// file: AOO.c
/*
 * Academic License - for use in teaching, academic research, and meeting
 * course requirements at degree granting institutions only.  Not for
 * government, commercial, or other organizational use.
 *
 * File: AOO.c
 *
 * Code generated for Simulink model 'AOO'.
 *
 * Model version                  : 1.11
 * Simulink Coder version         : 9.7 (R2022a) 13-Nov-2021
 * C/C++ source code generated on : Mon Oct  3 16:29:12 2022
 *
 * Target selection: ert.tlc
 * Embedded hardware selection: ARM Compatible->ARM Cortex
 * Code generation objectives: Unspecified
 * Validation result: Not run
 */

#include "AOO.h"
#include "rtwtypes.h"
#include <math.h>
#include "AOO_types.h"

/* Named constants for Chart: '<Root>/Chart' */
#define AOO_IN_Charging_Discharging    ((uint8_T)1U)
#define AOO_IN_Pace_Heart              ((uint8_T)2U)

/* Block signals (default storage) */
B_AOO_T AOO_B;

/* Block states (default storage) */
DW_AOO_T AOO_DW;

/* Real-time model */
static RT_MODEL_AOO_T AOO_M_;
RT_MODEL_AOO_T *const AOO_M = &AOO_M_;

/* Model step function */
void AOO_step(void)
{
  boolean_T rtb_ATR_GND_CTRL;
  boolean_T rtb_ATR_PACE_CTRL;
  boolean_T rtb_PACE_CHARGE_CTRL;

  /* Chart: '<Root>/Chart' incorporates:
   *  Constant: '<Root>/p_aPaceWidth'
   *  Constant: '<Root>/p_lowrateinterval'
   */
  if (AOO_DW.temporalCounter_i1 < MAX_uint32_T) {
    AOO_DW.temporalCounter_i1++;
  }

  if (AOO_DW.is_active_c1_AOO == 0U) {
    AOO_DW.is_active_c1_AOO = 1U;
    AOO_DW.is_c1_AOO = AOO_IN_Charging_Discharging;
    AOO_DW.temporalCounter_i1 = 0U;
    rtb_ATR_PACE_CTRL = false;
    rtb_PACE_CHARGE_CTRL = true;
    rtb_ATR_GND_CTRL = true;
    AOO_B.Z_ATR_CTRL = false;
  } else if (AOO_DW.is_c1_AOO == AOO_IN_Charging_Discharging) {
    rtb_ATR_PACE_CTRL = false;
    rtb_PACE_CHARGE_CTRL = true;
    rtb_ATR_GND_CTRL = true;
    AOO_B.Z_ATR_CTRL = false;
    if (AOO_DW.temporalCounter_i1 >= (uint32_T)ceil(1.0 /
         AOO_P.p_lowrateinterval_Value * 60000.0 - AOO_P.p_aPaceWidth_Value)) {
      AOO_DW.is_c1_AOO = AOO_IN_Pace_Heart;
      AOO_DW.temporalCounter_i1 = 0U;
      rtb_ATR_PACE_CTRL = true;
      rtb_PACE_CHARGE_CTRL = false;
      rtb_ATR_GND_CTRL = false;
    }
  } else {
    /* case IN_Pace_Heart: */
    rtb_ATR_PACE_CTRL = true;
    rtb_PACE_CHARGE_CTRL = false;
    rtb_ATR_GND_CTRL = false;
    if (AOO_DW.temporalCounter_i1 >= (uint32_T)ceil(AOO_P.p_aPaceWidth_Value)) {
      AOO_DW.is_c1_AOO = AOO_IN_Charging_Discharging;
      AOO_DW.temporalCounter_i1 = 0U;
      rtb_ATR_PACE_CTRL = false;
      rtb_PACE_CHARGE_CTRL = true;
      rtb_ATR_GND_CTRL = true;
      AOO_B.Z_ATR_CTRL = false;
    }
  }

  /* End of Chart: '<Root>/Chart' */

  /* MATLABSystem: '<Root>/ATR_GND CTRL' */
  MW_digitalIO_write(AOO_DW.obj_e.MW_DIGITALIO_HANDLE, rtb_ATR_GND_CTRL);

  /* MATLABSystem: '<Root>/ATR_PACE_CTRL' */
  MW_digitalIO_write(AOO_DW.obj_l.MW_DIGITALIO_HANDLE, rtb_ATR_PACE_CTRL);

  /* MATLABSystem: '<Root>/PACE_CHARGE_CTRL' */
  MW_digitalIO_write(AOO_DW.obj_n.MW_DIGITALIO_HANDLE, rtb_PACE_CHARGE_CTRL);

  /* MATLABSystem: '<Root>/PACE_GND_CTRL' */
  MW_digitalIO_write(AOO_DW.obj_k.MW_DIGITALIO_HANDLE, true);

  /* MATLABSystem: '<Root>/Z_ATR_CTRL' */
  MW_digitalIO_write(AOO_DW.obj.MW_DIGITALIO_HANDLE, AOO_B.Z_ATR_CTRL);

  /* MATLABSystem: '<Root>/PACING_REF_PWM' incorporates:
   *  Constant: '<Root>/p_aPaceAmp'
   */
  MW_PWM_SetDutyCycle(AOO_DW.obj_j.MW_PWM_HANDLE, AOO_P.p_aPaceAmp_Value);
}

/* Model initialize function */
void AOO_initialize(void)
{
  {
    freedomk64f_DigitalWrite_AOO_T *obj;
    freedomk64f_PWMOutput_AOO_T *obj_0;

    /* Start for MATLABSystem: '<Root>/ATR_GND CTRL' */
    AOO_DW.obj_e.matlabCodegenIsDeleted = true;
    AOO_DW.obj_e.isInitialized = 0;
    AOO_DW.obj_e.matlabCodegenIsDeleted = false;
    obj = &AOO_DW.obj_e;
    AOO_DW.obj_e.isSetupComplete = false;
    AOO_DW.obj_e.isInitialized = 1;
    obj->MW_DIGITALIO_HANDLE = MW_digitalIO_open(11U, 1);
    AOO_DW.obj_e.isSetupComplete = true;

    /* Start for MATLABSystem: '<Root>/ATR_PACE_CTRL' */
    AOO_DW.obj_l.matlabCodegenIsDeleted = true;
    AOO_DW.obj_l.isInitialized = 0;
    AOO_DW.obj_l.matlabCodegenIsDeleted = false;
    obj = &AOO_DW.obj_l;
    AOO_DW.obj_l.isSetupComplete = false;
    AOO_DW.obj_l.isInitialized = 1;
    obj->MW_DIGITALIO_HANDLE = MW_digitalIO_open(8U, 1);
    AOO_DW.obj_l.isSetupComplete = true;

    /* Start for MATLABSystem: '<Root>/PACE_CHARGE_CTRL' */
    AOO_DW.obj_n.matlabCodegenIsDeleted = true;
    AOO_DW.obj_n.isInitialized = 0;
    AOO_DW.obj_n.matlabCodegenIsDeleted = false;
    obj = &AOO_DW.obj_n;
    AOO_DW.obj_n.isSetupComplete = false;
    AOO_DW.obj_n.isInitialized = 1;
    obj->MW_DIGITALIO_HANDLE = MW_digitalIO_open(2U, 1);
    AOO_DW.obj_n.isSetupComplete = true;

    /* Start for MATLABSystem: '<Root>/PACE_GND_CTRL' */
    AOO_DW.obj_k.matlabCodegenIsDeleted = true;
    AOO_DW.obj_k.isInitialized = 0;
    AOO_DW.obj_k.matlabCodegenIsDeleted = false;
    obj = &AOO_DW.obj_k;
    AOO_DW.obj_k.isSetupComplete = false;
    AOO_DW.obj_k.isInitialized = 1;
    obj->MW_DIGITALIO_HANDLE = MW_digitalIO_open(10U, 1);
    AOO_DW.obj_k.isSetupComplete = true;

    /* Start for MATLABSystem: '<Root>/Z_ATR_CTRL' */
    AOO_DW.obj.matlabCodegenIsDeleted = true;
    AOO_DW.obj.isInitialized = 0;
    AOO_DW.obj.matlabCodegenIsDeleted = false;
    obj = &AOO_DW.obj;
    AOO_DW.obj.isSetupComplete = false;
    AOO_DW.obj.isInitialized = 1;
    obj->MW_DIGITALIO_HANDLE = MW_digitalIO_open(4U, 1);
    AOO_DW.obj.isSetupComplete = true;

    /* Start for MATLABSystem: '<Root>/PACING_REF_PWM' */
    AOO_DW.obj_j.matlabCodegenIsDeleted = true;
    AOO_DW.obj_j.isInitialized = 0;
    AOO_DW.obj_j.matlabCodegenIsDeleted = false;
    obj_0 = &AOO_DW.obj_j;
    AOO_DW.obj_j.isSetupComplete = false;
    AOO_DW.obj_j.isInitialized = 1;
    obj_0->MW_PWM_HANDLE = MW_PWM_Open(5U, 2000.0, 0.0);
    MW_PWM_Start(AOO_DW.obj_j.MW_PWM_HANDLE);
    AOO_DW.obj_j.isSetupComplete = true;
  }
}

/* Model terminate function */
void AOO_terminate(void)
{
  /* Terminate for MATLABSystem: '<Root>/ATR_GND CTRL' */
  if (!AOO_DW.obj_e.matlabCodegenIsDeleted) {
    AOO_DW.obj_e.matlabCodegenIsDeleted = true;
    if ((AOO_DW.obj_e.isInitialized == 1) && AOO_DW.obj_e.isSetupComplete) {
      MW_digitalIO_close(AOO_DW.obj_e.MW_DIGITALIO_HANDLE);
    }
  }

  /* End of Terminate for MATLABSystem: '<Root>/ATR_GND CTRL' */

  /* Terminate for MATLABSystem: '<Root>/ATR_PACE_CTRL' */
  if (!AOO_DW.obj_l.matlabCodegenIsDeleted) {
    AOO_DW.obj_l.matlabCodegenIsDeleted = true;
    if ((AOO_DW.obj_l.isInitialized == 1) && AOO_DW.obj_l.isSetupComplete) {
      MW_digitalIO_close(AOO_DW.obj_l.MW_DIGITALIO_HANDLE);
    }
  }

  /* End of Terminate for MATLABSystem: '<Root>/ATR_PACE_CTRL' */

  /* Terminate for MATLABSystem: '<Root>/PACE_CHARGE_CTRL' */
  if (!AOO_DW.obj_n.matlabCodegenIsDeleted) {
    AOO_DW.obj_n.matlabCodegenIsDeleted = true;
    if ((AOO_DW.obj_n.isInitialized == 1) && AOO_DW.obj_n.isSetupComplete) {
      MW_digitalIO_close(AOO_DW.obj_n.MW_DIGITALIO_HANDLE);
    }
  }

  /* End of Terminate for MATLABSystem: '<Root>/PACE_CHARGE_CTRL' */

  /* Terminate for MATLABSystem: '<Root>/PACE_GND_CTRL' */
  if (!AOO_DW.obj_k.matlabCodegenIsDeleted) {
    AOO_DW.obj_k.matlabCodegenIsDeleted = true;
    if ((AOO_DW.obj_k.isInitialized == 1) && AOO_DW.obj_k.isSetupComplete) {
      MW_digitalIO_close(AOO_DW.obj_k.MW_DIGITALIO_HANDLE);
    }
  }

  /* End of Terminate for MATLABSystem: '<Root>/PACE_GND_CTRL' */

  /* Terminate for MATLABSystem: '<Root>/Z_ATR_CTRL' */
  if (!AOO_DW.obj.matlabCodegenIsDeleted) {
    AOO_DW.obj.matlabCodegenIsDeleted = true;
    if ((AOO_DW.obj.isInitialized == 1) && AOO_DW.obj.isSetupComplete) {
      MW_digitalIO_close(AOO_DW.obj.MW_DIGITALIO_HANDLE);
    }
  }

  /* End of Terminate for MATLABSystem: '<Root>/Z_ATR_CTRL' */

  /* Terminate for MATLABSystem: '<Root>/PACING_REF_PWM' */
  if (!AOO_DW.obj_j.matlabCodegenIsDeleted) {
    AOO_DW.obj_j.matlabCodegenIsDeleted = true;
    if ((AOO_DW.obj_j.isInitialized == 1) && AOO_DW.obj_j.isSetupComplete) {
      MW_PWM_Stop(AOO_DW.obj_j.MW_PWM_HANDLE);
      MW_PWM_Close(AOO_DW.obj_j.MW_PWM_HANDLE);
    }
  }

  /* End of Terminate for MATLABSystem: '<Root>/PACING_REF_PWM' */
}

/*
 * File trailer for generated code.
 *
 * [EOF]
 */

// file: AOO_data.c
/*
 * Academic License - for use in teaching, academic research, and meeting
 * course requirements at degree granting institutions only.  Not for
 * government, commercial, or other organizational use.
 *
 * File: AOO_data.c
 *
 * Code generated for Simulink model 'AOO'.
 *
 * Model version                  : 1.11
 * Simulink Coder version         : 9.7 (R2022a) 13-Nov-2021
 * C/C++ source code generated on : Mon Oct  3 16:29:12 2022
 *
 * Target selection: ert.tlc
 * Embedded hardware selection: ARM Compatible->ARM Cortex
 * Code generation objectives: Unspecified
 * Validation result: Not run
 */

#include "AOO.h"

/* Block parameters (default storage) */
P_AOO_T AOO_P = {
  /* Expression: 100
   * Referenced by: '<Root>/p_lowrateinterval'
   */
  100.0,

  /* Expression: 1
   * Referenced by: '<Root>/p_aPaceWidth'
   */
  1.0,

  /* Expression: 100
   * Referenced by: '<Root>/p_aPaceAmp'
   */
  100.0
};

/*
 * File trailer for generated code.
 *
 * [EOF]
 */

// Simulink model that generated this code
simulink model "AOO"  (R2022a)
settings: Solver=FixedStepAuto  StartTime=0.0  StopTime=10.0  FixedStep=1e-3  RelTol=1e-3  EnableMultiTasking=on
undefined symbols (not defined in the file): D10, D11, D2, D4, D5, D8, PTA0, PTA2, PTB23, PTB9, PTD0, PTD2
libraries: frdmk64flib x6

== system AOO ==
  ATR_GND CTRL : frdmk64flib/Digital Write  Whichpin=PTD2 (D11)
  ATR_PACE_CTRL : frdmk64flib/Digital Write  Whichpin=PTA0 (D8)
  Chart : Stateflow chart  TreatAsAtomicUnit=on
  PACE_CHARGE_CTRL : frdmk64flib/Digital Write  Whichpin=PTB9 (D2)
  PACE_GND_CTRL : frdmk64flib/Digital Write  Whichpin=PTD0 (D10)
  PACING_REF_PWM : frdmk64flib/PWM Output  Whichpin=PTA2 (D5)  InitialFrequency=2000  InitialDutyCycle=0
  Requirements Table : Requirements Table  TreatAsAtomicUnit=on
  Z_ATR_CTRL : frdmk64flib/Digital Write  Whichpin=PTB23 (D4)
  p_aPaceAmp : Constant  Value=100
  p_aPaceWidth : Constant
  p_lowrateinterval : Constant
  wires:
  p_aPaceWidth/1 -> Chart/1(rate_limit)
  p_lowrateinterval/1 -> Chart/2(pulse_width)
  p_aPaceAmp/1 -> PACING_REF_PWM/1
  Chart/5(ATR_GND_CTRL) -> ATR_GND CTRL/1
  Chart/4(ATR_PACE_CTRL) -> ATR_PACE_CTRL/1
  Chart/3(PACE_GND_CTRL) -> PACE_GND_CTRL/1
  Chart/2(Z_ATR_CTRL) -> Z_ATR_CTRL/1
  Chart/1(PACE_CHARGE_CTRL) -> PACE_CHARGE_CTRL/1

== stateflow chart AOO/Chart ==
  state Charging_Discharging
    entry:
    ATR_PACE_CTRL = false
    PACE_CHARGE_CTRL = true
    ATR_GND_CTRL = true
    PACE_GND_CTRL = true
    Z_ATR_CTRL=false
  state Pace_Heart
    entry:
    ATR_PACE_CTRL = true
    PACE_CHARGE_CTRL = false
    PACE_GND_CTRL = true
    ATR_GND_CTRL = false
  (default) -> Charging_Discharging
  Charging_Discharging -> Pace_Heart : after(((1/rate_limit)*60000)-pulse_width,msec)
  Pace_Heart -> Charging_Discharging : after(pulse_width,msec)
  data: rate_limit input; pulse_width input; PACE_CHARGE_CTRL output boolean; Z_ATR_CTRL output boolean; PACE_GND_CTRL output boolean; ATR_PACE_CTRL output boolean; ATR_GND_CTRL output boolean

== stateflow chart AOO/Requirements Table ==
  (default) -> (junction 1073741860)
  (junction 1073741860) -> (junction 1073741861) : {
      | % SF_REQ_REV_07
      | }
  (junction 1073741861) -> (junction 1073741863) : {
      | % HEADER_ASSIGNMENTS
      |
      | }
  (junction 1073741863) -> (junction 1073741865) : {
      | % START_A_4
      | }
  (junction 1073741865) -> (junction 1073741867) : {
      | }
  (junction 1073741867) -> (junction 1073741869)
  (junction 1073741869) -> (junction 1073741871) : {
      | }
  (junction 1073741871) -> (junction 1073741873) : {
      | % END_A_4
      | }
  (junction 1073741873) -> (junction 1073741898) : {
      | % START_R_1
      | }
  (junction 1073741898) -> (junction 1073741900) : {
      | }
  (junction 1073741900) -> (junction 1073741902) : {
      |
      |
      | }
  (junction 1073741902) -> (junction 1073741904) : {
      | }
  (junction 1073741904) -> (junction 1073741906) : {
      | % END_R_1
      | }
